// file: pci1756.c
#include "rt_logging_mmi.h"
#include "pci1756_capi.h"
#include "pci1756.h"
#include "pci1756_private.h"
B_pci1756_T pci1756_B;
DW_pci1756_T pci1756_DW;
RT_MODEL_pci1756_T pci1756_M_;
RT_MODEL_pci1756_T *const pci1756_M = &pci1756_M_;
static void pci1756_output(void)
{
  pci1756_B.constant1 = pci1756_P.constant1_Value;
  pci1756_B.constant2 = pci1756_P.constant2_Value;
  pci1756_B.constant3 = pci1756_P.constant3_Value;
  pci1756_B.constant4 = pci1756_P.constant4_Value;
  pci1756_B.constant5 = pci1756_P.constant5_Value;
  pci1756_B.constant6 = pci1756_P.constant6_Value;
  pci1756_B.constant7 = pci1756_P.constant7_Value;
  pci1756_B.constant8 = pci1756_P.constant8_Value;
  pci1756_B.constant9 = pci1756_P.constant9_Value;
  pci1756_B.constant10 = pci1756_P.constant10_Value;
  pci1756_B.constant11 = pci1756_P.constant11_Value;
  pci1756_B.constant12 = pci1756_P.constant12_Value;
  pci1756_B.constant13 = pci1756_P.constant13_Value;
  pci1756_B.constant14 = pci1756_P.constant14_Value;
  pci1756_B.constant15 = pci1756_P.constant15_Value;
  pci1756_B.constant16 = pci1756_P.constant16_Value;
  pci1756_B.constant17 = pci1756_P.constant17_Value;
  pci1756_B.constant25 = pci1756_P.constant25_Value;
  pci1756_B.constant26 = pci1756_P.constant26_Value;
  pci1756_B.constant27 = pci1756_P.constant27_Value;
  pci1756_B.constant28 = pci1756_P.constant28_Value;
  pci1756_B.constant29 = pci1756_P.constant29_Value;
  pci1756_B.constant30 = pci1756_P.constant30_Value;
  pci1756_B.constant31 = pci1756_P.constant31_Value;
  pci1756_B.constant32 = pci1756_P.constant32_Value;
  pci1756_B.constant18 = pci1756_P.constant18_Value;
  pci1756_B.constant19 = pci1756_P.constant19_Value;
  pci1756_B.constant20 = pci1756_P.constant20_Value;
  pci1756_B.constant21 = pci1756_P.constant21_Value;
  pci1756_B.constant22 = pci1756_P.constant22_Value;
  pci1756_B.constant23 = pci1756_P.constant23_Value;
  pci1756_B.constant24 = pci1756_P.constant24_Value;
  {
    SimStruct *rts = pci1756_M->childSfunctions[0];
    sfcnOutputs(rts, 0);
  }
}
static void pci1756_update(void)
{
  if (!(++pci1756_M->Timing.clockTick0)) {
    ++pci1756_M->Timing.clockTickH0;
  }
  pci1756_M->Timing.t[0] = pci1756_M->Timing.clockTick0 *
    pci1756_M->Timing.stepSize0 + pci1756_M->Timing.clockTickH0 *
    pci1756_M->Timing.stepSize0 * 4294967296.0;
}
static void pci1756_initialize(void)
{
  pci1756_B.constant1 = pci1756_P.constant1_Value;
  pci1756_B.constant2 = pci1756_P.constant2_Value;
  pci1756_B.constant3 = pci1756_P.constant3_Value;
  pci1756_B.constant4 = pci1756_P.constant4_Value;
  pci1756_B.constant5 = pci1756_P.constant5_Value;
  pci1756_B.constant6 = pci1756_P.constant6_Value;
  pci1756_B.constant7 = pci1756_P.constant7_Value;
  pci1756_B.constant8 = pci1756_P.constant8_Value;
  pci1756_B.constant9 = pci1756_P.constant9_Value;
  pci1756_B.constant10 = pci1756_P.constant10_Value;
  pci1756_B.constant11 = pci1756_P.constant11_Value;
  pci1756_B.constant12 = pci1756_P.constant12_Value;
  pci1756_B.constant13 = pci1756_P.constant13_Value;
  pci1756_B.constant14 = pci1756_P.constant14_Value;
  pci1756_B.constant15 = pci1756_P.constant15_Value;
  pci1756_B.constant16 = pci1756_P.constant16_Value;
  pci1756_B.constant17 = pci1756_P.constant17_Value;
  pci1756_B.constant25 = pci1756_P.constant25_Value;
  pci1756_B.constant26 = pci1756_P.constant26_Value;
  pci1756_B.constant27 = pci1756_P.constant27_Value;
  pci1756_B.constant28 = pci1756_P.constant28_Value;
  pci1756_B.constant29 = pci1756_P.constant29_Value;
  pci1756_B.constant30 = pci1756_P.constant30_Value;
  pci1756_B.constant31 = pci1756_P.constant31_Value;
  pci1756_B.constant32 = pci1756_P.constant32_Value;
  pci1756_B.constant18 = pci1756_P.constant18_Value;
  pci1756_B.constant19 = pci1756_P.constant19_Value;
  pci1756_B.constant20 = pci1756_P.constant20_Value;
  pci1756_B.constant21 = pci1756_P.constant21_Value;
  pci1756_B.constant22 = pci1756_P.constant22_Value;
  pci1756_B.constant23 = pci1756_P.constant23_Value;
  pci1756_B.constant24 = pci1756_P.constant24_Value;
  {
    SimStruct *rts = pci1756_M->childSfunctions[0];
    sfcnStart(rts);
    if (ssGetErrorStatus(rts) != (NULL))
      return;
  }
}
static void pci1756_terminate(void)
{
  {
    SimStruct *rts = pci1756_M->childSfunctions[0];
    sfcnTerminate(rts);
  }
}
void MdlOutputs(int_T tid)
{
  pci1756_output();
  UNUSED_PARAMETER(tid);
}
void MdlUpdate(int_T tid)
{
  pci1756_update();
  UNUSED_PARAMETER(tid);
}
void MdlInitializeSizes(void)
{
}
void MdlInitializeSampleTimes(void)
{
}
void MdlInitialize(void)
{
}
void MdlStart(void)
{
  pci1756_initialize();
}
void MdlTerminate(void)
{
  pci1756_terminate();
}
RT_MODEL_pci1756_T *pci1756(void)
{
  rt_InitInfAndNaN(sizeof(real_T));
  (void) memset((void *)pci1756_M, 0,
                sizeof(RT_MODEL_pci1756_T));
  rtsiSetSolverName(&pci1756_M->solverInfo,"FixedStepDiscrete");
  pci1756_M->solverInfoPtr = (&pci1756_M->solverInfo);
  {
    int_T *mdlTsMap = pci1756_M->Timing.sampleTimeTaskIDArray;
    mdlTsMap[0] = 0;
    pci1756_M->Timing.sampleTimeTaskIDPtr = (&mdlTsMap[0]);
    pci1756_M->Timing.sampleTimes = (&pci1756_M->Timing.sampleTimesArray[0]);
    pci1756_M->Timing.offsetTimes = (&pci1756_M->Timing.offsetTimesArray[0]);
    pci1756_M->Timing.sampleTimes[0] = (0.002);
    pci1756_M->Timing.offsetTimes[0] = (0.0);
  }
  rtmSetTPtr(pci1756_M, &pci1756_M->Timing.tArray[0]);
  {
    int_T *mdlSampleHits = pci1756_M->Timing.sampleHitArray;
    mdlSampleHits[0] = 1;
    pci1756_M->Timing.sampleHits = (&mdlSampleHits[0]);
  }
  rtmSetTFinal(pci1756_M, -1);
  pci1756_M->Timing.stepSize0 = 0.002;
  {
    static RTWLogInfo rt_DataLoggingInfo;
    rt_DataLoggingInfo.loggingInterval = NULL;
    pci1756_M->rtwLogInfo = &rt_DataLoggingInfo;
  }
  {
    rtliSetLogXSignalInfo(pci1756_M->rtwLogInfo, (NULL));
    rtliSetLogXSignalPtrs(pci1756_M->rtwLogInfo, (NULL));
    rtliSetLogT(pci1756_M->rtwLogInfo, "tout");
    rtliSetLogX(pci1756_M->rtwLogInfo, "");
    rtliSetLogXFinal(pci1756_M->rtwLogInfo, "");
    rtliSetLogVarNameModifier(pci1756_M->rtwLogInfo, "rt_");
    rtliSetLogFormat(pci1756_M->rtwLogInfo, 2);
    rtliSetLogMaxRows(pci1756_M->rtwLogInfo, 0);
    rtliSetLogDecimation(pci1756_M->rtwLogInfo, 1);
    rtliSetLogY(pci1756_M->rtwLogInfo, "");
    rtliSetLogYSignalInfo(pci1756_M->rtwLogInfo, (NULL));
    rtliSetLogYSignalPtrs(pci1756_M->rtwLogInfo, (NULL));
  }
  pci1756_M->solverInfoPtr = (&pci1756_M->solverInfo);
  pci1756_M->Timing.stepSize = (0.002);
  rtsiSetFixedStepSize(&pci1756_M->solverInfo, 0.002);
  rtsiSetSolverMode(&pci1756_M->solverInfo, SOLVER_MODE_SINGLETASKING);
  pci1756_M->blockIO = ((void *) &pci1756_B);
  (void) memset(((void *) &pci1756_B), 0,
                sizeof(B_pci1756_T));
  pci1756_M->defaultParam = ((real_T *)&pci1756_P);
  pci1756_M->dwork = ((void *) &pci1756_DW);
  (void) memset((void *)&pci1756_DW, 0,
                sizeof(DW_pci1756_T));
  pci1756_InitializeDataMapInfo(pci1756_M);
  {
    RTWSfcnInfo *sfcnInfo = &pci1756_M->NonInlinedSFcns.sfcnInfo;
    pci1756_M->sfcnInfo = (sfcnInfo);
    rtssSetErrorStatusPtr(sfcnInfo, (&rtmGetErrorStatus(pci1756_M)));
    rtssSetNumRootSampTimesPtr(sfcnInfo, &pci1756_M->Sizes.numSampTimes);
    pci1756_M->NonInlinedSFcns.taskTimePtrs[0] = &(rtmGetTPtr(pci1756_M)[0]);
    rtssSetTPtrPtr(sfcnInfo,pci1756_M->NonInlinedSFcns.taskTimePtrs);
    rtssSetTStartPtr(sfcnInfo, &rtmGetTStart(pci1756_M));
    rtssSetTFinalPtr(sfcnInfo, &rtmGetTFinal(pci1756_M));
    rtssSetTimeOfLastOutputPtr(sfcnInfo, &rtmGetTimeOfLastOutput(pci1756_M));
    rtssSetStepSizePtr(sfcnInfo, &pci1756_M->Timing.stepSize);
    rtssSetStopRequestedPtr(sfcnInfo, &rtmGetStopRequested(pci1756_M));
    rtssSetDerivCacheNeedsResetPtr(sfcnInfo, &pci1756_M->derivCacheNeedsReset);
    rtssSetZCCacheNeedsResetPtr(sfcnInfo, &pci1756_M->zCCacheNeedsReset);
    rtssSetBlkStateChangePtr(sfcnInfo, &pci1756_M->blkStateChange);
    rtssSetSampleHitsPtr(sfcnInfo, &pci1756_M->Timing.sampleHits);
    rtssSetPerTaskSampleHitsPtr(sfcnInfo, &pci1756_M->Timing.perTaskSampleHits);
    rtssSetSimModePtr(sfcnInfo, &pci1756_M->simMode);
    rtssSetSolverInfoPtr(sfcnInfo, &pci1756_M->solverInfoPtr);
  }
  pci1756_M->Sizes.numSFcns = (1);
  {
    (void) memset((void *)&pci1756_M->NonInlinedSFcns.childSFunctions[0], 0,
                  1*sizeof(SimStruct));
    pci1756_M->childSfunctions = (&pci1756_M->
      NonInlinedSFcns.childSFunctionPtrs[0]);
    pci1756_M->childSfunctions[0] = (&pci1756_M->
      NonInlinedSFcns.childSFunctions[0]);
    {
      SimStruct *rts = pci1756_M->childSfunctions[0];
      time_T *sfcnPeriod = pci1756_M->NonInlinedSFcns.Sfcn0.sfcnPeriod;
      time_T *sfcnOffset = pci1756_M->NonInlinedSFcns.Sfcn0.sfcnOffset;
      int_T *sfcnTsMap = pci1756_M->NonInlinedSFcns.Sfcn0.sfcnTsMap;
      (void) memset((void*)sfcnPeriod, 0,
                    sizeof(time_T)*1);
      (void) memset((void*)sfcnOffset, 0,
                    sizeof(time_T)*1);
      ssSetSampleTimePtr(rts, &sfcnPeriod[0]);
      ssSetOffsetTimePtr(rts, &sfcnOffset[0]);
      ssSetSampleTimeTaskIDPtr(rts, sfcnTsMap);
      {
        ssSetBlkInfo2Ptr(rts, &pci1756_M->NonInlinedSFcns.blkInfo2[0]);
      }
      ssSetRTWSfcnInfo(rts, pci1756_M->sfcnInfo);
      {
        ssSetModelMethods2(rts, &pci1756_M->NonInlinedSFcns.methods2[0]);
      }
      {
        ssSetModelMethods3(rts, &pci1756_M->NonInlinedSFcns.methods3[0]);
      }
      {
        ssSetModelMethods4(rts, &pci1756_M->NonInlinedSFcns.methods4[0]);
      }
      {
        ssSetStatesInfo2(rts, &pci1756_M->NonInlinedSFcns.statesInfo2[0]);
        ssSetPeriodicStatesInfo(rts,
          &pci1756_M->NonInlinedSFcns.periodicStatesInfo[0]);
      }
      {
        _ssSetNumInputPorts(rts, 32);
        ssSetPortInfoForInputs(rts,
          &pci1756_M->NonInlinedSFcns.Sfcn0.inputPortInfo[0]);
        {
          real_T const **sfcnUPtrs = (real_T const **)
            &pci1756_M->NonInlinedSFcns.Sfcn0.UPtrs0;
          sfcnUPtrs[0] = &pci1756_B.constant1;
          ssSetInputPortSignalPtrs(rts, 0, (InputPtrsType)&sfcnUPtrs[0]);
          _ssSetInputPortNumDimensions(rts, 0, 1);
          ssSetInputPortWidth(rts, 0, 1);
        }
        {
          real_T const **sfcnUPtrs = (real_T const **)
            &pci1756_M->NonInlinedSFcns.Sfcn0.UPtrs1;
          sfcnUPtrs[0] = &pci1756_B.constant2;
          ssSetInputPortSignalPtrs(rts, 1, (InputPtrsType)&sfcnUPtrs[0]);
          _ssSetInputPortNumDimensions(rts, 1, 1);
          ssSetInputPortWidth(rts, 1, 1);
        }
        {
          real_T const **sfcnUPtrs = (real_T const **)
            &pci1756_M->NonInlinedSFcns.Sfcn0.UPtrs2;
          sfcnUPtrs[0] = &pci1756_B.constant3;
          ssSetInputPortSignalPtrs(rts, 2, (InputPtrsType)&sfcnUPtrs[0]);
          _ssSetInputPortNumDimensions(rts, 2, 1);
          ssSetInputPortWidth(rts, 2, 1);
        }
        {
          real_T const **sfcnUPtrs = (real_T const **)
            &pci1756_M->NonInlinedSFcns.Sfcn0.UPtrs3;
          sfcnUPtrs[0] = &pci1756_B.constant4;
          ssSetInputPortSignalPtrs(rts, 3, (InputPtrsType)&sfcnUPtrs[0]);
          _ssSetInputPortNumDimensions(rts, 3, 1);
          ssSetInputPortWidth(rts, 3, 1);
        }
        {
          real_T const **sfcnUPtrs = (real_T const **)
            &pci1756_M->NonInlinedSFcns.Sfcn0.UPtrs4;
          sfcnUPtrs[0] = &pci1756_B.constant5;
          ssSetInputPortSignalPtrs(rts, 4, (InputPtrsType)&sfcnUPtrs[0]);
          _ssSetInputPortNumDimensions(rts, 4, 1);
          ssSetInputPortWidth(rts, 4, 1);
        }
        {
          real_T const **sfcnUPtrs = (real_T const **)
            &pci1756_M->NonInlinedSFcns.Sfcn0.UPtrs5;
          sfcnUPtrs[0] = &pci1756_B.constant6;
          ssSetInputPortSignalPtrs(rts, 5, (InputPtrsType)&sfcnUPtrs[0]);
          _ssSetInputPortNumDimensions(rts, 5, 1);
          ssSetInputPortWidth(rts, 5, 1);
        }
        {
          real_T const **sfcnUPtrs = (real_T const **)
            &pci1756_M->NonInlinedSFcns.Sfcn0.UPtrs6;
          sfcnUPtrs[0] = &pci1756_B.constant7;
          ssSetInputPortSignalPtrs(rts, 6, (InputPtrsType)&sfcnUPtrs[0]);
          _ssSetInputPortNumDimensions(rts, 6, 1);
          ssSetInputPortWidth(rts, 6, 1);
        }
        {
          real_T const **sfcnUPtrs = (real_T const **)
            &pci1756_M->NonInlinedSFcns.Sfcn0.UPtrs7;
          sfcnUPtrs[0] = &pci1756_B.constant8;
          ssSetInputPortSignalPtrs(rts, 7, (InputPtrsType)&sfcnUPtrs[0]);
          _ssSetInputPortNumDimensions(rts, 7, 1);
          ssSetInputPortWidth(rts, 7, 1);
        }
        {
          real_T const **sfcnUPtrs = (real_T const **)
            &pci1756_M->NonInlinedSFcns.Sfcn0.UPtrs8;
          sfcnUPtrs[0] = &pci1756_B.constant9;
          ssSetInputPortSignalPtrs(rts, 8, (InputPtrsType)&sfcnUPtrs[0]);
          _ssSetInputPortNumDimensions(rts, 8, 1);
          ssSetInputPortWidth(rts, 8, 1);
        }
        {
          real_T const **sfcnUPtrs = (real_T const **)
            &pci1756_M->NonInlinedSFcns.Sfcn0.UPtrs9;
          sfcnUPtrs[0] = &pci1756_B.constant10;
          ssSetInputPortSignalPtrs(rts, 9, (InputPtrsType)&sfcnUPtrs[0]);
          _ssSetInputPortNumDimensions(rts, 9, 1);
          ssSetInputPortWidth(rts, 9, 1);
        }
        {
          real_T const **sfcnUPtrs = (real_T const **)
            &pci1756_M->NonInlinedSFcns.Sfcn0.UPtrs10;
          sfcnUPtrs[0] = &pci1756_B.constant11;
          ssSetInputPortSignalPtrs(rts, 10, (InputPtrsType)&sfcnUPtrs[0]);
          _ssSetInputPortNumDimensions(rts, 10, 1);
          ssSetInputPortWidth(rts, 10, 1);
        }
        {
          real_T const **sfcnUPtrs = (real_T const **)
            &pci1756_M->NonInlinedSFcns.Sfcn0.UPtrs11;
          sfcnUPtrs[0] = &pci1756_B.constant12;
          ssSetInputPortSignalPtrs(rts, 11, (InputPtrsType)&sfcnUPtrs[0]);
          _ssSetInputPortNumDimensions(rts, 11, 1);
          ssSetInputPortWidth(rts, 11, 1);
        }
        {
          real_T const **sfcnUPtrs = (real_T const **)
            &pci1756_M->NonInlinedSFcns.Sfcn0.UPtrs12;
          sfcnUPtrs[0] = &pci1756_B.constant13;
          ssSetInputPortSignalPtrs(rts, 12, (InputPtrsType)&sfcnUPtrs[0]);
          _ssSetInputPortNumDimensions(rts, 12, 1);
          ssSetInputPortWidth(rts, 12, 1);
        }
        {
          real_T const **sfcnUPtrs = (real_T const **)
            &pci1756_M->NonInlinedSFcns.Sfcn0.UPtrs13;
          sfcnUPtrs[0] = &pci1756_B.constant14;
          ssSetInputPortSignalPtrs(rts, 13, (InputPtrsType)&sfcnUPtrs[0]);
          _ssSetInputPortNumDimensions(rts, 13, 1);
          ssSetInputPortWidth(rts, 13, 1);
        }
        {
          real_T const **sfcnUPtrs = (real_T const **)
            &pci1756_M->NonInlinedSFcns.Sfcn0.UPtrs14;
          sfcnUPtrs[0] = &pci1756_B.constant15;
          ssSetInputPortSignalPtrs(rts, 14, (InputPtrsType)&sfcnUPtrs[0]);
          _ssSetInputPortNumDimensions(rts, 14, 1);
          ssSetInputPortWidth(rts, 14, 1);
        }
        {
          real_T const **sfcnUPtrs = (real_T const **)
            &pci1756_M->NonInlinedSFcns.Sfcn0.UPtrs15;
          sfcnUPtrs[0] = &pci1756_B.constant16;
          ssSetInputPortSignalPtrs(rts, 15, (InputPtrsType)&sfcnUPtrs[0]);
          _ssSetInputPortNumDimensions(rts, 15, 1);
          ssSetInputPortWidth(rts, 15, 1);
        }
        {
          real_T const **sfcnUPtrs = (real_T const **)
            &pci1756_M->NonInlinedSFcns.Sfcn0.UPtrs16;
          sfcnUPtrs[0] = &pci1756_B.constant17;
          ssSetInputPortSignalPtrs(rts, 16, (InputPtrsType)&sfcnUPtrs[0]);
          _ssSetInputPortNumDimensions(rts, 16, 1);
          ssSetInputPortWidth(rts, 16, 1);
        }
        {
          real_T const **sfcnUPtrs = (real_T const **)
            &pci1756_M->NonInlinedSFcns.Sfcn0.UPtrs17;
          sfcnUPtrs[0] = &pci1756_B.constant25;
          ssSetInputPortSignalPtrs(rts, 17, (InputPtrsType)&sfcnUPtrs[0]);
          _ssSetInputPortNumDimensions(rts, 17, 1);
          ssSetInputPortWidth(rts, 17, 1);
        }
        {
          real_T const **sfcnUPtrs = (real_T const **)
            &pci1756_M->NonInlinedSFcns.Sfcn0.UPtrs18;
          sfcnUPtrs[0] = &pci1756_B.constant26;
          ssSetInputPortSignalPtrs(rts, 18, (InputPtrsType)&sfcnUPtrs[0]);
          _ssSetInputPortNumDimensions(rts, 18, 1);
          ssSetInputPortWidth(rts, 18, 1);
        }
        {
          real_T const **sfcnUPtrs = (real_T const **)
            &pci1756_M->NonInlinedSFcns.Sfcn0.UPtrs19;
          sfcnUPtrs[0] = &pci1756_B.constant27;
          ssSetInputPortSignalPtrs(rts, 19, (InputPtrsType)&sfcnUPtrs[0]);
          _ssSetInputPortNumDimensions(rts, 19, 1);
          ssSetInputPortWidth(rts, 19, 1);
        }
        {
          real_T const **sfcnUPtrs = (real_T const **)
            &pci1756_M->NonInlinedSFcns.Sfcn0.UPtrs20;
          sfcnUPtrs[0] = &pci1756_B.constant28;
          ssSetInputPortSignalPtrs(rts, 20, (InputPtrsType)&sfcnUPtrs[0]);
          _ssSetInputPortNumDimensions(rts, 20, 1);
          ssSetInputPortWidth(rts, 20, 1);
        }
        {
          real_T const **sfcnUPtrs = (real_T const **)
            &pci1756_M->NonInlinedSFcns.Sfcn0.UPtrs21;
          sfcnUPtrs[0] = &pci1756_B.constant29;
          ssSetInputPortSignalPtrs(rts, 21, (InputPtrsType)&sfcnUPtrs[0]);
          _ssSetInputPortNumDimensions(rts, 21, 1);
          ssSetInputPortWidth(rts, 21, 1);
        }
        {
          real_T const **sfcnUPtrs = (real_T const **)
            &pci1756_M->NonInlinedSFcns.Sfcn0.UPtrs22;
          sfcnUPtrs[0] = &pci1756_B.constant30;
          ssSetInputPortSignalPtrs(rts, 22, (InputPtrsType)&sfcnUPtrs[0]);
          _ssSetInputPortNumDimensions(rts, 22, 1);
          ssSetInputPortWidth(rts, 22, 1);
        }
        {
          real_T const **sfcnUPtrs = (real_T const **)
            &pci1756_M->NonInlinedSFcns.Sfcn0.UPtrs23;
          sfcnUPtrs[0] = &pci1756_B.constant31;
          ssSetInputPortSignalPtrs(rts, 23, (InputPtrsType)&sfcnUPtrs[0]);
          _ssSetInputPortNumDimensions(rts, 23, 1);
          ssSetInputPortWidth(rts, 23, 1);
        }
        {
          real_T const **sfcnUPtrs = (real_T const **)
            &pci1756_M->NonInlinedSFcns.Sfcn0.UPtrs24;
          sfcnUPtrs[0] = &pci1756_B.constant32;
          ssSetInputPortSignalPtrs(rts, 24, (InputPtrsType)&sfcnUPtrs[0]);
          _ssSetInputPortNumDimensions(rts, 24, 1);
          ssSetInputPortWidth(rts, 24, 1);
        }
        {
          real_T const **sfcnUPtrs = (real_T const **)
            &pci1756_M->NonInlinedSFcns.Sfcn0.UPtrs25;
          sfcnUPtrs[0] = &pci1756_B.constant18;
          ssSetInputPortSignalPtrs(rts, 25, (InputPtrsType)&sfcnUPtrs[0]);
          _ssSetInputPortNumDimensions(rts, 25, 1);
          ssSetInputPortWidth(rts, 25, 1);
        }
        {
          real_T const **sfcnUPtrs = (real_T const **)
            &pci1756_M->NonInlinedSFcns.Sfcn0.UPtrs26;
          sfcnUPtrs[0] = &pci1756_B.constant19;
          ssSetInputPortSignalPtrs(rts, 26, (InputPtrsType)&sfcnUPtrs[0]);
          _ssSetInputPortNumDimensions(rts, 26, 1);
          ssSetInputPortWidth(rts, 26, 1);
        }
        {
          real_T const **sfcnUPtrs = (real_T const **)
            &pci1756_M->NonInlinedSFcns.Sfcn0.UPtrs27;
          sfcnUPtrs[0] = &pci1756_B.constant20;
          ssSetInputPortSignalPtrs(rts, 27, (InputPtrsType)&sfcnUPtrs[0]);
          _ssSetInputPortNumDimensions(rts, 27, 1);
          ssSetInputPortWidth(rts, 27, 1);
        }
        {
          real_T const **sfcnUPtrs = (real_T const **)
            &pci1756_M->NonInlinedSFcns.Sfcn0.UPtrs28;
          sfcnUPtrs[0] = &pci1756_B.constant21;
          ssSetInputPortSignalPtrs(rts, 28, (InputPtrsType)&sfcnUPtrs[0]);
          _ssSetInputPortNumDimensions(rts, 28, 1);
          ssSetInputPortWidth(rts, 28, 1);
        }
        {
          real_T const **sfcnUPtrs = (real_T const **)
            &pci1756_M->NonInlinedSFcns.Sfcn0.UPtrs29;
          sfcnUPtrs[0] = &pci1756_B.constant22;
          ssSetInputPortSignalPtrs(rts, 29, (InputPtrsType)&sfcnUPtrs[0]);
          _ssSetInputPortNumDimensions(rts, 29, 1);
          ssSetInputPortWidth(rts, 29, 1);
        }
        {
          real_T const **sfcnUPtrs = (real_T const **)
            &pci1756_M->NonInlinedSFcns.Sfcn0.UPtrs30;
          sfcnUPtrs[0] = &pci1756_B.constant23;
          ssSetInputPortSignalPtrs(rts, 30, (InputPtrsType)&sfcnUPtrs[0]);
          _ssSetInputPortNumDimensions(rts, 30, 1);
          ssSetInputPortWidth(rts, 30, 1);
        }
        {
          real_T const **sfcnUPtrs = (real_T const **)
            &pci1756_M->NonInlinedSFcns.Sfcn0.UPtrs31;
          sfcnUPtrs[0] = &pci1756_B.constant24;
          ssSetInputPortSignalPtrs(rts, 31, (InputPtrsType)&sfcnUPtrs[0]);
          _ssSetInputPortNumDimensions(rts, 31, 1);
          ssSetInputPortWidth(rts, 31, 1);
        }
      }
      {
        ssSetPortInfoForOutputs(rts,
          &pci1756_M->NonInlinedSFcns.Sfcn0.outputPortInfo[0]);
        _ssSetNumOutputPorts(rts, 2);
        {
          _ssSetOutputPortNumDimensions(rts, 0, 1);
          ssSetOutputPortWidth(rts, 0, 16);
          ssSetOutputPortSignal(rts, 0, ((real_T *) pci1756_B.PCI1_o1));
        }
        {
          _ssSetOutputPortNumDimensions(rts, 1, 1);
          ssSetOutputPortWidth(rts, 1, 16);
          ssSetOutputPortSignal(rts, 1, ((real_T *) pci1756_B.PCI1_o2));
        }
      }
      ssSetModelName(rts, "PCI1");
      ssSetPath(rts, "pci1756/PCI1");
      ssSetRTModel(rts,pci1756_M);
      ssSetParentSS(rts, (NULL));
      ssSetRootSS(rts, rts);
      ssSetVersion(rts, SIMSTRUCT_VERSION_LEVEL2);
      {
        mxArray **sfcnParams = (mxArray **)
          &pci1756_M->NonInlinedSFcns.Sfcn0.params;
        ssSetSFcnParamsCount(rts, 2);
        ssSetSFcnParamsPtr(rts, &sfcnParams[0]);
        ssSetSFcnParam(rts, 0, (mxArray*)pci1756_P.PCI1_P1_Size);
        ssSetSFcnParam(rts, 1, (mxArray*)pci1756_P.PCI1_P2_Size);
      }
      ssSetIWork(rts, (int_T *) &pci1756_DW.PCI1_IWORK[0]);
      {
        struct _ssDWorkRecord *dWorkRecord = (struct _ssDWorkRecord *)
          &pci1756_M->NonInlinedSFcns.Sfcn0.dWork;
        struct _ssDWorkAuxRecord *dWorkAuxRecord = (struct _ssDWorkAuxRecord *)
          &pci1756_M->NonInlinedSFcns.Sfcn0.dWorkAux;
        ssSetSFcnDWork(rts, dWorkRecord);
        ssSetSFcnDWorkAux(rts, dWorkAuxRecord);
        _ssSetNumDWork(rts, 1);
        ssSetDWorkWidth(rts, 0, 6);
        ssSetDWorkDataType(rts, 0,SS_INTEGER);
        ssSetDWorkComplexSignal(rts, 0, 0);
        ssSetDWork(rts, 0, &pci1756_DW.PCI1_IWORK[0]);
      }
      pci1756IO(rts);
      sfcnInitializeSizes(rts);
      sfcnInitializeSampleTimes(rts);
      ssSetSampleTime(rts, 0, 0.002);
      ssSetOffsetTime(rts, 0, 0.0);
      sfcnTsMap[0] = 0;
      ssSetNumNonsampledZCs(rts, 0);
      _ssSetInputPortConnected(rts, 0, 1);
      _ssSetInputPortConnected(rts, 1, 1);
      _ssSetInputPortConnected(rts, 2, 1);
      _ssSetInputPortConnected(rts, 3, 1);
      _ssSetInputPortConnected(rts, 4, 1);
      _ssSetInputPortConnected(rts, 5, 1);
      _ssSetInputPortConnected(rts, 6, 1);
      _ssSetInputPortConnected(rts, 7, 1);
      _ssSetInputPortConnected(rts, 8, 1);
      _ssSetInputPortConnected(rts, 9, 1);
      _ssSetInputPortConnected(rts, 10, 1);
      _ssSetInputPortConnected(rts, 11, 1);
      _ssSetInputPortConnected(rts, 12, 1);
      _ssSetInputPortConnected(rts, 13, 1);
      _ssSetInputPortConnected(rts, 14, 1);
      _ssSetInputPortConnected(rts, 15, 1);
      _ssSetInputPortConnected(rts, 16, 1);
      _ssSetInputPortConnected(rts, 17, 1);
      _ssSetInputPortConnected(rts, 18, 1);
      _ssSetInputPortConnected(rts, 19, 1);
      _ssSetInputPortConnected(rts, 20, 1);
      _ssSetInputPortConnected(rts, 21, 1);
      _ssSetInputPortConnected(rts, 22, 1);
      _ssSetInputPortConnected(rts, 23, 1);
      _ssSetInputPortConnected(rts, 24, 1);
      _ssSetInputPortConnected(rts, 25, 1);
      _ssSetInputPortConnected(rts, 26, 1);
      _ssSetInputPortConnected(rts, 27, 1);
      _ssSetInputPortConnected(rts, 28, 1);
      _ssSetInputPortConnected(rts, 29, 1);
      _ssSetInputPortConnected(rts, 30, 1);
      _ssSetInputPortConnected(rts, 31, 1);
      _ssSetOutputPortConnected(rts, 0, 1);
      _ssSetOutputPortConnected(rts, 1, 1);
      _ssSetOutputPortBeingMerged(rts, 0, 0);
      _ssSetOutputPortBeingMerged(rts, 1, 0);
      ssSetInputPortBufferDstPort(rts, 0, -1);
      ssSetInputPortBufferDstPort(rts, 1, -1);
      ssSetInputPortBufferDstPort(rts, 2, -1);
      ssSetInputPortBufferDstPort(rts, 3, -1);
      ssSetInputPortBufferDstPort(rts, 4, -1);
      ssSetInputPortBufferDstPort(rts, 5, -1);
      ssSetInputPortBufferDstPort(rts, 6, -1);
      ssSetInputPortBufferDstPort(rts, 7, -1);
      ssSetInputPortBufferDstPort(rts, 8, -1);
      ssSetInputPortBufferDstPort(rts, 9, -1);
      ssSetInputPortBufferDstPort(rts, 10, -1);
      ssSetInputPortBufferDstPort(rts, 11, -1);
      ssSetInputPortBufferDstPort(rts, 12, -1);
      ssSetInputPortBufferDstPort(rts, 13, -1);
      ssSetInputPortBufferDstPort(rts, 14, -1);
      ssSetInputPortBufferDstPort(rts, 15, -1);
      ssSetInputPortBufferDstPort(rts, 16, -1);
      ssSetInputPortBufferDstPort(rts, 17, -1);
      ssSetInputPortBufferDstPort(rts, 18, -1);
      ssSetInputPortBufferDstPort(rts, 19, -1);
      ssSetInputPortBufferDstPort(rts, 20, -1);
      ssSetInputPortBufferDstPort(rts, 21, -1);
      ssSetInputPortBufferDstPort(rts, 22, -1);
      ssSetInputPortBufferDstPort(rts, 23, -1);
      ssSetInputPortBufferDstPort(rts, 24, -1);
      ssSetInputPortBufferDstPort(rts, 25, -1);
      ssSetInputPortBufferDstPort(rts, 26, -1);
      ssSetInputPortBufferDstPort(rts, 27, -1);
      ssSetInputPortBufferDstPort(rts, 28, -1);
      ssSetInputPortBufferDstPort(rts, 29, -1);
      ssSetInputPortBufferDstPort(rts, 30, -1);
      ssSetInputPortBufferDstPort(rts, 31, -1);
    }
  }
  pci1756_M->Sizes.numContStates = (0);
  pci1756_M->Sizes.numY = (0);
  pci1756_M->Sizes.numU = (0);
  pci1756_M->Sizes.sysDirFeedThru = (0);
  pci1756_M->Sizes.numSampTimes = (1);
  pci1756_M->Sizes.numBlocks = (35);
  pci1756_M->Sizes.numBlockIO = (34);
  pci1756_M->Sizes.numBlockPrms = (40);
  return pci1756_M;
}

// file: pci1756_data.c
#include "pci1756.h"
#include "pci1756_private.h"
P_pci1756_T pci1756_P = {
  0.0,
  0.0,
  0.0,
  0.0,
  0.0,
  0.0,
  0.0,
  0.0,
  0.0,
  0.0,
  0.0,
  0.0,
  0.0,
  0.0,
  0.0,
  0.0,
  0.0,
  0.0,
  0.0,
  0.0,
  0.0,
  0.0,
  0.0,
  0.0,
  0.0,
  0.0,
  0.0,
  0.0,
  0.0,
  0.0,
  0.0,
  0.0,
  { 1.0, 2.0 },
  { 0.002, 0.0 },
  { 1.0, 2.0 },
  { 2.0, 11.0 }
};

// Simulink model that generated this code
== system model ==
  PCI1 : S-Function  FunctionName=pci1756IO  <- 1: constant1, 2: constant2, 3: constant3, 4: constant4, 5: constant5, 6: constant6, 7: constant7, 8: constant8, 9: constant9, 10: constant10, 11: constant11, 12: constant12, 13: constant13, 14: constant14, 15: constant15, 16: constant16, 17: constant17, 18: constant25, 19: constant26, 20: constant27, 21: constant28, 22: constant29, 23: constant30, 24: constant31, 25: constant32, 26: constant18, 27: constant19, 28: constant20, 29: constant21, 30: constant22, 31: constant23, 32: constant24
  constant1 : Constant  Value=0
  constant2 : Constant  Value=0
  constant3 : Constant  Value=0
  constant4 : Constant  Value=0
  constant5 : Constant  Value=0
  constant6 : Constant  Value=0
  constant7 : Constant  Value=0
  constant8 : Constant  Value=0
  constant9 : Constant  Value=0
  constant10 : Constant  Value=0
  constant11 : Constant  Value=0
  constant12 : Constant  Value=0
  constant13 : Constant  Value=0
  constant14 : Constant  Value=0
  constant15 : Constant  Value=0
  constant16 : Constant  Value=0
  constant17 : Constant  Value=0
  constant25 : Constant  Value=0
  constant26 : Constant  Value=0
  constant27 : Constant  Value=0
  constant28 : Constant  Value=0
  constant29 : Constant  Value=0
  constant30 : Constant  Value=0
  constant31 : Constant  Value=0
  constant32 : Constant  Value=0
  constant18 : Constant  Value=0
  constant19 : Constant  Value=0
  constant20 : Constant  Value=0
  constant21 : Constant  Value=0
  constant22 : Constant  Value=0
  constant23 : Constant  Value=0
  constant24 : Constant  Value=0
